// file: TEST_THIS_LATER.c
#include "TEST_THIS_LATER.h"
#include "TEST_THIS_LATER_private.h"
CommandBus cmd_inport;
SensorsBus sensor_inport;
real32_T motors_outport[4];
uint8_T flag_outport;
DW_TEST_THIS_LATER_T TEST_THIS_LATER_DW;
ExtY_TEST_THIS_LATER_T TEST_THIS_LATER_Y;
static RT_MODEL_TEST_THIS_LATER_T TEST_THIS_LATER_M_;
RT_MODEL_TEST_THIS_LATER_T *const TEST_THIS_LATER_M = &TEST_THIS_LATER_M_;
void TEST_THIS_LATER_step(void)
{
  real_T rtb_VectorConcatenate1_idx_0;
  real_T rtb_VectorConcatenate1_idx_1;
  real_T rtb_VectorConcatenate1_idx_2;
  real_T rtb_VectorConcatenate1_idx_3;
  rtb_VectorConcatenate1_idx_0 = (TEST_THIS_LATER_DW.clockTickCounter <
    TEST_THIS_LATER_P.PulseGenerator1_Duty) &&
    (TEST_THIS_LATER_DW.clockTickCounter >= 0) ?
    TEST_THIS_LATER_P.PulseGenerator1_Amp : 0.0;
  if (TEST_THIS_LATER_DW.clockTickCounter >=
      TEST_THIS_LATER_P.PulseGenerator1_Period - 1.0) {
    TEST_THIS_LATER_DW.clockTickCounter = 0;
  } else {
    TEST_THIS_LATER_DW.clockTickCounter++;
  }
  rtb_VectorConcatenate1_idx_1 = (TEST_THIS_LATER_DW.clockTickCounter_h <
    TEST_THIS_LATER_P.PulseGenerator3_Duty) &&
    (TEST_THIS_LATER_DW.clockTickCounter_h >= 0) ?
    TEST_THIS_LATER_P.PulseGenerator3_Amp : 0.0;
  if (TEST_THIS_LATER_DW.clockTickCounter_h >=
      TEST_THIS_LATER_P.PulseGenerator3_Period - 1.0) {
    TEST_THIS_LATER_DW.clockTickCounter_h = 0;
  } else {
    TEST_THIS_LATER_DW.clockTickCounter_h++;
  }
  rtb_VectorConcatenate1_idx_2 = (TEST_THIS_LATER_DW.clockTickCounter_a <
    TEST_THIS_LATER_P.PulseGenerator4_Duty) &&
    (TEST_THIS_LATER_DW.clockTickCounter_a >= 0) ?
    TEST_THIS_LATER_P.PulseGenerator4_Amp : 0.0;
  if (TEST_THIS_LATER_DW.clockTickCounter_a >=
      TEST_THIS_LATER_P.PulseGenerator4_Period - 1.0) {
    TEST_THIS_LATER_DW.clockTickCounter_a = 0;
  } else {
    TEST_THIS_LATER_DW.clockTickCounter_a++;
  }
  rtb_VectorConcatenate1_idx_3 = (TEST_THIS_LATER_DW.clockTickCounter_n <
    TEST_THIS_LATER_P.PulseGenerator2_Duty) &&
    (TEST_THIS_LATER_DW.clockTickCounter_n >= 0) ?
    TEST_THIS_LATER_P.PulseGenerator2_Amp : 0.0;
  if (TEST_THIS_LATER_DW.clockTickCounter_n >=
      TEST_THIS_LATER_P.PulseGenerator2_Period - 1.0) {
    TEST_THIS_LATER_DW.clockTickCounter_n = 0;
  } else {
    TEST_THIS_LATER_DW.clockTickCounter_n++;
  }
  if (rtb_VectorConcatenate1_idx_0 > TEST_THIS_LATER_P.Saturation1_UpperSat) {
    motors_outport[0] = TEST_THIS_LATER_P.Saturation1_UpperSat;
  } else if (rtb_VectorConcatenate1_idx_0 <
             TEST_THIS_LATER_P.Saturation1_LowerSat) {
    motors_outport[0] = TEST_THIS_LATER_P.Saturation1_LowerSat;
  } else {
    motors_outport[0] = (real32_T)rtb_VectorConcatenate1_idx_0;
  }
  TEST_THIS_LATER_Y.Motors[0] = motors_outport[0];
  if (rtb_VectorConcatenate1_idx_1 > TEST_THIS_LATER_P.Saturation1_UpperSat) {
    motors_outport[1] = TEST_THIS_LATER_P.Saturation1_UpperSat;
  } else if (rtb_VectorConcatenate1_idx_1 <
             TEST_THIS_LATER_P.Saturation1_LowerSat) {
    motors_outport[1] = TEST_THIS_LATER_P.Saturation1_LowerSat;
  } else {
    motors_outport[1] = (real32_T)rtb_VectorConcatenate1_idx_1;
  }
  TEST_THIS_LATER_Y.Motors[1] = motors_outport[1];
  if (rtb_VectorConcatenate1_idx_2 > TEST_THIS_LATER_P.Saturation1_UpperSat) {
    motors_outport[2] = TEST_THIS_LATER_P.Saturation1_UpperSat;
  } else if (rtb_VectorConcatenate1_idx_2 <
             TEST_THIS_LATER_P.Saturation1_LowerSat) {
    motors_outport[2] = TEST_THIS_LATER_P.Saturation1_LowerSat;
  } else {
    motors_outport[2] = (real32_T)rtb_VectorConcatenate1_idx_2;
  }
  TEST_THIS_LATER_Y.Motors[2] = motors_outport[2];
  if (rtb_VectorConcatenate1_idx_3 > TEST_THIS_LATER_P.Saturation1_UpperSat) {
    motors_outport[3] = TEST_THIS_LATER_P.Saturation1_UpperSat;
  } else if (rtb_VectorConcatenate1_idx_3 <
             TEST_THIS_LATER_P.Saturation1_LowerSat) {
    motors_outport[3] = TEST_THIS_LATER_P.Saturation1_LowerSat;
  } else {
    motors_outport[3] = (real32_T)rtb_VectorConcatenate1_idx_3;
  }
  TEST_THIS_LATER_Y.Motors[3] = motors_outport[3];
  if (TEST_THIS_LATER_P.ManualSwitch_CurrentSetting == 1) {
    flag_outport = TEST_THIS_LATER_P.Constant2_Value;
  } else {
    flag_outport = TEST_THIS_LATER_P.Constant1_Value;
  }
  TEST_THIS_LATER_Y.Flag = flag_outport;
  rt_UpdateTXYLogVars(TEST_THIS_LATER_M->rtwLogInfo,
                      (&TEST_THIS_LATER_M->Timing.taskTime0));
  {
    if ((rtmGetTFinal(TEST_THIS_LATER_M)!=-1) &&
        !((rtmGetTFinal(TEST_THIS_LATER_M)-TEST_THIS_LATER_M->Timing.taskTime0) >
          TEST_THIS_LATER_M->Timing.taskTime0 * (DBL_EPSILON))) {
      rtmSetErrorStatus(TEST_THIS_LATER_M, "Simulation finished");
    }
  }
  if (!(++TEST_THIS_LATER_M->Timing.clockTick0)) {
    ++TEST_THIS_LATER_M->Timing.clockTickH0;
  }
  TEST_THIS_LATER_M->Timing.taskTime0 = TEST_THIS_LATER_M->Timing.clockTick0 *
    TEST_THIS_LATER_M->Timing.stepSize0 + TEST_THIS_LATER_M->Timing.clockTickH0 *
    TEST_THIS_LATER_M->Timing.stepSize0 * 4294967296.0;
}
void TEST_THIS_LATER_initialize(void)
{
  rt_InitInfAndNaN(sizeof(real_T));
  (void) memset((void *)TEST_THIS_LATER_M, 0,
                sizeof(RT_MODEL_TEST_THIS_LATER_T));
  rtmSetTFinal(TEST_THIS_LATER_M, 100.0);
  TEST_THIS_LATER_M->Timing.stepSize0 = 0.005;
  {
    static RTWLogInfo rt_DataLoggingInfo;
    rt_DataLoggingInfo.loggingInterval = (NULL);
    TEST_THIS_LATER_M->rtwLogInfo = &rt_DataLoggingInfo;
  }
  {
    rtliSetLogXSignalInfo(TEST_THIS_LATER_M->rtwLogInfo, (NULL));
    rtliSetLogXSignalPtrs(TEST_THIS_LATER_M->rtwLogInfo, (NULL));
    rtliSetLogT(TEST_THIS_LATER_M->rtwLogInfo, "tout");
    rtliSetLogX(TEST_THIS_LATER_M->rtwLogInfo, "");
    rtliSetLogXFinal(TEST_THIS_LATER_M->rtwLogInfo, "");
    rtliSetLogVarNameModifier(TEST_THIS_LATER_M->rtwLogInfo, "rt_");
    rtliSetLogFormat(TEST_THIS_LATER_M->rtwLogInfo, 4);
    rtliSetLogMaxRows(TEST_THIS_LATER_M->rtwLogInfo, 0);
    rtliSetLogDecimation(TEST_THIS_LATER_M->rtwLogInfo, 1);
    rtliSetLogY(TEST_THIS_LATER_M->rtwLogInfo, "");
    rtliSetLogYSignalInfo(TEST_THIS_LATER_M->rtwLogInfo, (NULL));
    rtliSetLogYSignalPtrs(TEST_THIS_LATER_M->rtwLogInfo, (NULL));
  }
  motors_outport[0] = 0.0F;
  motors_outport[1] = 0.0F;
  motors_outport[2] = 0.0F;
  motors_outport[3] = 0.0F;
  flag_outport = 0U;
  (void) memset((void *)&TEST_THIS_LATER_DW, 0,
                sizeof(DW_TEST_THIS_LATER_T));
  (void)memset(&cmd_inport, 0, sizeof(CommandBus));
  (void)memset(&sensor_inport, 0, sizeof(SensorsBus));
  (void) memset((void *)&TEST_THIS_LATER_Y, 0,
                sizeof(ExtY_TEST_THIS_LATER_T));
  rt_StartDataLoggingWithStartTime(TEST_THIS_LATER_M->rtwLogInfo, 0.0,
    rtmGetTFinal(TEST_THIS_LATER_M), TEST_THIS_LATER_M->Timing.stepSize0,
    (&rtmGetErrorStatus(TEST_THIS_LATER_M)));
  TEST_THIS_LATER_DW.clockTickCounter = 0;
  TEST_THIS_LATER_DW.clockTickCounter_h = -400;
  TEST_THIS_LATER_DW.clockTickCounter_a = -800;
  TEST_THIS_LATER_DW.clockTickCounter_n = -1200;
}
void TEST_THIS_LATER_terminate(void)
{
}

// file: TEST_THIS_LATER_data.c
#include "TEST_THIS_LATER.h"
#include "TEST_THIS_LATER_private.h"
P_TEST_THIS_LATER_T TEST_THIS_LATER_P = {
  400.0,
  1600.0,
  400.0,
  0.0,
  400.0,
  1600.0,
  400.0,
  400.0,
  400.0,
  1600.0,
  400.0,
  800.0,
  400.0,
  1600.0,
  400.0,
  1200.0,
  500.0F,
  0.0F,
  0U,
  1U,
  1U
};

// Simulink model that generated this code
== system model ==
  Inport#1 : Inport
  Inport#2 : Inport
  Motors : Outport  <- 1: Saturation1
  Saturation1 : Saturate  UpperLimit=500  LowerLimit=0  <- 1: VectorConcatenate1
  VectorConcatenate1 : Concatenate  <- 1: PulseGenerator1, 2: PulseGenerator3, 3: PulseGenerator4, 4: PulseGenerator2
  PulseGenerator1 : DiscretePulseGenerator  Amplitude=400  Period=1600  PulseWidth=400
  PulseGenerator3 : DiscretePulseGenerator  Amplitude=400  Period=1600  PulseWidth=400  PhaseDelay=400
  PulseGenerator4 : DiscretePulseGenerator  Amplitude=400  Period=1600  PulseWidth=400  PhaseDelay=800
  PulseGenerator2 : DiscretePulseGenerator  Amplitude=400  Period=1600  PulseWidth=400  PhaseDelay=1200
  Flag : Outport  <- 1: ManualSwitch
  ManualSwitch : ManualSwitch  <- 1: Constant2, 2: Constant1
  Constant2 : Constant  Value=0
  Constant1 : Constant
